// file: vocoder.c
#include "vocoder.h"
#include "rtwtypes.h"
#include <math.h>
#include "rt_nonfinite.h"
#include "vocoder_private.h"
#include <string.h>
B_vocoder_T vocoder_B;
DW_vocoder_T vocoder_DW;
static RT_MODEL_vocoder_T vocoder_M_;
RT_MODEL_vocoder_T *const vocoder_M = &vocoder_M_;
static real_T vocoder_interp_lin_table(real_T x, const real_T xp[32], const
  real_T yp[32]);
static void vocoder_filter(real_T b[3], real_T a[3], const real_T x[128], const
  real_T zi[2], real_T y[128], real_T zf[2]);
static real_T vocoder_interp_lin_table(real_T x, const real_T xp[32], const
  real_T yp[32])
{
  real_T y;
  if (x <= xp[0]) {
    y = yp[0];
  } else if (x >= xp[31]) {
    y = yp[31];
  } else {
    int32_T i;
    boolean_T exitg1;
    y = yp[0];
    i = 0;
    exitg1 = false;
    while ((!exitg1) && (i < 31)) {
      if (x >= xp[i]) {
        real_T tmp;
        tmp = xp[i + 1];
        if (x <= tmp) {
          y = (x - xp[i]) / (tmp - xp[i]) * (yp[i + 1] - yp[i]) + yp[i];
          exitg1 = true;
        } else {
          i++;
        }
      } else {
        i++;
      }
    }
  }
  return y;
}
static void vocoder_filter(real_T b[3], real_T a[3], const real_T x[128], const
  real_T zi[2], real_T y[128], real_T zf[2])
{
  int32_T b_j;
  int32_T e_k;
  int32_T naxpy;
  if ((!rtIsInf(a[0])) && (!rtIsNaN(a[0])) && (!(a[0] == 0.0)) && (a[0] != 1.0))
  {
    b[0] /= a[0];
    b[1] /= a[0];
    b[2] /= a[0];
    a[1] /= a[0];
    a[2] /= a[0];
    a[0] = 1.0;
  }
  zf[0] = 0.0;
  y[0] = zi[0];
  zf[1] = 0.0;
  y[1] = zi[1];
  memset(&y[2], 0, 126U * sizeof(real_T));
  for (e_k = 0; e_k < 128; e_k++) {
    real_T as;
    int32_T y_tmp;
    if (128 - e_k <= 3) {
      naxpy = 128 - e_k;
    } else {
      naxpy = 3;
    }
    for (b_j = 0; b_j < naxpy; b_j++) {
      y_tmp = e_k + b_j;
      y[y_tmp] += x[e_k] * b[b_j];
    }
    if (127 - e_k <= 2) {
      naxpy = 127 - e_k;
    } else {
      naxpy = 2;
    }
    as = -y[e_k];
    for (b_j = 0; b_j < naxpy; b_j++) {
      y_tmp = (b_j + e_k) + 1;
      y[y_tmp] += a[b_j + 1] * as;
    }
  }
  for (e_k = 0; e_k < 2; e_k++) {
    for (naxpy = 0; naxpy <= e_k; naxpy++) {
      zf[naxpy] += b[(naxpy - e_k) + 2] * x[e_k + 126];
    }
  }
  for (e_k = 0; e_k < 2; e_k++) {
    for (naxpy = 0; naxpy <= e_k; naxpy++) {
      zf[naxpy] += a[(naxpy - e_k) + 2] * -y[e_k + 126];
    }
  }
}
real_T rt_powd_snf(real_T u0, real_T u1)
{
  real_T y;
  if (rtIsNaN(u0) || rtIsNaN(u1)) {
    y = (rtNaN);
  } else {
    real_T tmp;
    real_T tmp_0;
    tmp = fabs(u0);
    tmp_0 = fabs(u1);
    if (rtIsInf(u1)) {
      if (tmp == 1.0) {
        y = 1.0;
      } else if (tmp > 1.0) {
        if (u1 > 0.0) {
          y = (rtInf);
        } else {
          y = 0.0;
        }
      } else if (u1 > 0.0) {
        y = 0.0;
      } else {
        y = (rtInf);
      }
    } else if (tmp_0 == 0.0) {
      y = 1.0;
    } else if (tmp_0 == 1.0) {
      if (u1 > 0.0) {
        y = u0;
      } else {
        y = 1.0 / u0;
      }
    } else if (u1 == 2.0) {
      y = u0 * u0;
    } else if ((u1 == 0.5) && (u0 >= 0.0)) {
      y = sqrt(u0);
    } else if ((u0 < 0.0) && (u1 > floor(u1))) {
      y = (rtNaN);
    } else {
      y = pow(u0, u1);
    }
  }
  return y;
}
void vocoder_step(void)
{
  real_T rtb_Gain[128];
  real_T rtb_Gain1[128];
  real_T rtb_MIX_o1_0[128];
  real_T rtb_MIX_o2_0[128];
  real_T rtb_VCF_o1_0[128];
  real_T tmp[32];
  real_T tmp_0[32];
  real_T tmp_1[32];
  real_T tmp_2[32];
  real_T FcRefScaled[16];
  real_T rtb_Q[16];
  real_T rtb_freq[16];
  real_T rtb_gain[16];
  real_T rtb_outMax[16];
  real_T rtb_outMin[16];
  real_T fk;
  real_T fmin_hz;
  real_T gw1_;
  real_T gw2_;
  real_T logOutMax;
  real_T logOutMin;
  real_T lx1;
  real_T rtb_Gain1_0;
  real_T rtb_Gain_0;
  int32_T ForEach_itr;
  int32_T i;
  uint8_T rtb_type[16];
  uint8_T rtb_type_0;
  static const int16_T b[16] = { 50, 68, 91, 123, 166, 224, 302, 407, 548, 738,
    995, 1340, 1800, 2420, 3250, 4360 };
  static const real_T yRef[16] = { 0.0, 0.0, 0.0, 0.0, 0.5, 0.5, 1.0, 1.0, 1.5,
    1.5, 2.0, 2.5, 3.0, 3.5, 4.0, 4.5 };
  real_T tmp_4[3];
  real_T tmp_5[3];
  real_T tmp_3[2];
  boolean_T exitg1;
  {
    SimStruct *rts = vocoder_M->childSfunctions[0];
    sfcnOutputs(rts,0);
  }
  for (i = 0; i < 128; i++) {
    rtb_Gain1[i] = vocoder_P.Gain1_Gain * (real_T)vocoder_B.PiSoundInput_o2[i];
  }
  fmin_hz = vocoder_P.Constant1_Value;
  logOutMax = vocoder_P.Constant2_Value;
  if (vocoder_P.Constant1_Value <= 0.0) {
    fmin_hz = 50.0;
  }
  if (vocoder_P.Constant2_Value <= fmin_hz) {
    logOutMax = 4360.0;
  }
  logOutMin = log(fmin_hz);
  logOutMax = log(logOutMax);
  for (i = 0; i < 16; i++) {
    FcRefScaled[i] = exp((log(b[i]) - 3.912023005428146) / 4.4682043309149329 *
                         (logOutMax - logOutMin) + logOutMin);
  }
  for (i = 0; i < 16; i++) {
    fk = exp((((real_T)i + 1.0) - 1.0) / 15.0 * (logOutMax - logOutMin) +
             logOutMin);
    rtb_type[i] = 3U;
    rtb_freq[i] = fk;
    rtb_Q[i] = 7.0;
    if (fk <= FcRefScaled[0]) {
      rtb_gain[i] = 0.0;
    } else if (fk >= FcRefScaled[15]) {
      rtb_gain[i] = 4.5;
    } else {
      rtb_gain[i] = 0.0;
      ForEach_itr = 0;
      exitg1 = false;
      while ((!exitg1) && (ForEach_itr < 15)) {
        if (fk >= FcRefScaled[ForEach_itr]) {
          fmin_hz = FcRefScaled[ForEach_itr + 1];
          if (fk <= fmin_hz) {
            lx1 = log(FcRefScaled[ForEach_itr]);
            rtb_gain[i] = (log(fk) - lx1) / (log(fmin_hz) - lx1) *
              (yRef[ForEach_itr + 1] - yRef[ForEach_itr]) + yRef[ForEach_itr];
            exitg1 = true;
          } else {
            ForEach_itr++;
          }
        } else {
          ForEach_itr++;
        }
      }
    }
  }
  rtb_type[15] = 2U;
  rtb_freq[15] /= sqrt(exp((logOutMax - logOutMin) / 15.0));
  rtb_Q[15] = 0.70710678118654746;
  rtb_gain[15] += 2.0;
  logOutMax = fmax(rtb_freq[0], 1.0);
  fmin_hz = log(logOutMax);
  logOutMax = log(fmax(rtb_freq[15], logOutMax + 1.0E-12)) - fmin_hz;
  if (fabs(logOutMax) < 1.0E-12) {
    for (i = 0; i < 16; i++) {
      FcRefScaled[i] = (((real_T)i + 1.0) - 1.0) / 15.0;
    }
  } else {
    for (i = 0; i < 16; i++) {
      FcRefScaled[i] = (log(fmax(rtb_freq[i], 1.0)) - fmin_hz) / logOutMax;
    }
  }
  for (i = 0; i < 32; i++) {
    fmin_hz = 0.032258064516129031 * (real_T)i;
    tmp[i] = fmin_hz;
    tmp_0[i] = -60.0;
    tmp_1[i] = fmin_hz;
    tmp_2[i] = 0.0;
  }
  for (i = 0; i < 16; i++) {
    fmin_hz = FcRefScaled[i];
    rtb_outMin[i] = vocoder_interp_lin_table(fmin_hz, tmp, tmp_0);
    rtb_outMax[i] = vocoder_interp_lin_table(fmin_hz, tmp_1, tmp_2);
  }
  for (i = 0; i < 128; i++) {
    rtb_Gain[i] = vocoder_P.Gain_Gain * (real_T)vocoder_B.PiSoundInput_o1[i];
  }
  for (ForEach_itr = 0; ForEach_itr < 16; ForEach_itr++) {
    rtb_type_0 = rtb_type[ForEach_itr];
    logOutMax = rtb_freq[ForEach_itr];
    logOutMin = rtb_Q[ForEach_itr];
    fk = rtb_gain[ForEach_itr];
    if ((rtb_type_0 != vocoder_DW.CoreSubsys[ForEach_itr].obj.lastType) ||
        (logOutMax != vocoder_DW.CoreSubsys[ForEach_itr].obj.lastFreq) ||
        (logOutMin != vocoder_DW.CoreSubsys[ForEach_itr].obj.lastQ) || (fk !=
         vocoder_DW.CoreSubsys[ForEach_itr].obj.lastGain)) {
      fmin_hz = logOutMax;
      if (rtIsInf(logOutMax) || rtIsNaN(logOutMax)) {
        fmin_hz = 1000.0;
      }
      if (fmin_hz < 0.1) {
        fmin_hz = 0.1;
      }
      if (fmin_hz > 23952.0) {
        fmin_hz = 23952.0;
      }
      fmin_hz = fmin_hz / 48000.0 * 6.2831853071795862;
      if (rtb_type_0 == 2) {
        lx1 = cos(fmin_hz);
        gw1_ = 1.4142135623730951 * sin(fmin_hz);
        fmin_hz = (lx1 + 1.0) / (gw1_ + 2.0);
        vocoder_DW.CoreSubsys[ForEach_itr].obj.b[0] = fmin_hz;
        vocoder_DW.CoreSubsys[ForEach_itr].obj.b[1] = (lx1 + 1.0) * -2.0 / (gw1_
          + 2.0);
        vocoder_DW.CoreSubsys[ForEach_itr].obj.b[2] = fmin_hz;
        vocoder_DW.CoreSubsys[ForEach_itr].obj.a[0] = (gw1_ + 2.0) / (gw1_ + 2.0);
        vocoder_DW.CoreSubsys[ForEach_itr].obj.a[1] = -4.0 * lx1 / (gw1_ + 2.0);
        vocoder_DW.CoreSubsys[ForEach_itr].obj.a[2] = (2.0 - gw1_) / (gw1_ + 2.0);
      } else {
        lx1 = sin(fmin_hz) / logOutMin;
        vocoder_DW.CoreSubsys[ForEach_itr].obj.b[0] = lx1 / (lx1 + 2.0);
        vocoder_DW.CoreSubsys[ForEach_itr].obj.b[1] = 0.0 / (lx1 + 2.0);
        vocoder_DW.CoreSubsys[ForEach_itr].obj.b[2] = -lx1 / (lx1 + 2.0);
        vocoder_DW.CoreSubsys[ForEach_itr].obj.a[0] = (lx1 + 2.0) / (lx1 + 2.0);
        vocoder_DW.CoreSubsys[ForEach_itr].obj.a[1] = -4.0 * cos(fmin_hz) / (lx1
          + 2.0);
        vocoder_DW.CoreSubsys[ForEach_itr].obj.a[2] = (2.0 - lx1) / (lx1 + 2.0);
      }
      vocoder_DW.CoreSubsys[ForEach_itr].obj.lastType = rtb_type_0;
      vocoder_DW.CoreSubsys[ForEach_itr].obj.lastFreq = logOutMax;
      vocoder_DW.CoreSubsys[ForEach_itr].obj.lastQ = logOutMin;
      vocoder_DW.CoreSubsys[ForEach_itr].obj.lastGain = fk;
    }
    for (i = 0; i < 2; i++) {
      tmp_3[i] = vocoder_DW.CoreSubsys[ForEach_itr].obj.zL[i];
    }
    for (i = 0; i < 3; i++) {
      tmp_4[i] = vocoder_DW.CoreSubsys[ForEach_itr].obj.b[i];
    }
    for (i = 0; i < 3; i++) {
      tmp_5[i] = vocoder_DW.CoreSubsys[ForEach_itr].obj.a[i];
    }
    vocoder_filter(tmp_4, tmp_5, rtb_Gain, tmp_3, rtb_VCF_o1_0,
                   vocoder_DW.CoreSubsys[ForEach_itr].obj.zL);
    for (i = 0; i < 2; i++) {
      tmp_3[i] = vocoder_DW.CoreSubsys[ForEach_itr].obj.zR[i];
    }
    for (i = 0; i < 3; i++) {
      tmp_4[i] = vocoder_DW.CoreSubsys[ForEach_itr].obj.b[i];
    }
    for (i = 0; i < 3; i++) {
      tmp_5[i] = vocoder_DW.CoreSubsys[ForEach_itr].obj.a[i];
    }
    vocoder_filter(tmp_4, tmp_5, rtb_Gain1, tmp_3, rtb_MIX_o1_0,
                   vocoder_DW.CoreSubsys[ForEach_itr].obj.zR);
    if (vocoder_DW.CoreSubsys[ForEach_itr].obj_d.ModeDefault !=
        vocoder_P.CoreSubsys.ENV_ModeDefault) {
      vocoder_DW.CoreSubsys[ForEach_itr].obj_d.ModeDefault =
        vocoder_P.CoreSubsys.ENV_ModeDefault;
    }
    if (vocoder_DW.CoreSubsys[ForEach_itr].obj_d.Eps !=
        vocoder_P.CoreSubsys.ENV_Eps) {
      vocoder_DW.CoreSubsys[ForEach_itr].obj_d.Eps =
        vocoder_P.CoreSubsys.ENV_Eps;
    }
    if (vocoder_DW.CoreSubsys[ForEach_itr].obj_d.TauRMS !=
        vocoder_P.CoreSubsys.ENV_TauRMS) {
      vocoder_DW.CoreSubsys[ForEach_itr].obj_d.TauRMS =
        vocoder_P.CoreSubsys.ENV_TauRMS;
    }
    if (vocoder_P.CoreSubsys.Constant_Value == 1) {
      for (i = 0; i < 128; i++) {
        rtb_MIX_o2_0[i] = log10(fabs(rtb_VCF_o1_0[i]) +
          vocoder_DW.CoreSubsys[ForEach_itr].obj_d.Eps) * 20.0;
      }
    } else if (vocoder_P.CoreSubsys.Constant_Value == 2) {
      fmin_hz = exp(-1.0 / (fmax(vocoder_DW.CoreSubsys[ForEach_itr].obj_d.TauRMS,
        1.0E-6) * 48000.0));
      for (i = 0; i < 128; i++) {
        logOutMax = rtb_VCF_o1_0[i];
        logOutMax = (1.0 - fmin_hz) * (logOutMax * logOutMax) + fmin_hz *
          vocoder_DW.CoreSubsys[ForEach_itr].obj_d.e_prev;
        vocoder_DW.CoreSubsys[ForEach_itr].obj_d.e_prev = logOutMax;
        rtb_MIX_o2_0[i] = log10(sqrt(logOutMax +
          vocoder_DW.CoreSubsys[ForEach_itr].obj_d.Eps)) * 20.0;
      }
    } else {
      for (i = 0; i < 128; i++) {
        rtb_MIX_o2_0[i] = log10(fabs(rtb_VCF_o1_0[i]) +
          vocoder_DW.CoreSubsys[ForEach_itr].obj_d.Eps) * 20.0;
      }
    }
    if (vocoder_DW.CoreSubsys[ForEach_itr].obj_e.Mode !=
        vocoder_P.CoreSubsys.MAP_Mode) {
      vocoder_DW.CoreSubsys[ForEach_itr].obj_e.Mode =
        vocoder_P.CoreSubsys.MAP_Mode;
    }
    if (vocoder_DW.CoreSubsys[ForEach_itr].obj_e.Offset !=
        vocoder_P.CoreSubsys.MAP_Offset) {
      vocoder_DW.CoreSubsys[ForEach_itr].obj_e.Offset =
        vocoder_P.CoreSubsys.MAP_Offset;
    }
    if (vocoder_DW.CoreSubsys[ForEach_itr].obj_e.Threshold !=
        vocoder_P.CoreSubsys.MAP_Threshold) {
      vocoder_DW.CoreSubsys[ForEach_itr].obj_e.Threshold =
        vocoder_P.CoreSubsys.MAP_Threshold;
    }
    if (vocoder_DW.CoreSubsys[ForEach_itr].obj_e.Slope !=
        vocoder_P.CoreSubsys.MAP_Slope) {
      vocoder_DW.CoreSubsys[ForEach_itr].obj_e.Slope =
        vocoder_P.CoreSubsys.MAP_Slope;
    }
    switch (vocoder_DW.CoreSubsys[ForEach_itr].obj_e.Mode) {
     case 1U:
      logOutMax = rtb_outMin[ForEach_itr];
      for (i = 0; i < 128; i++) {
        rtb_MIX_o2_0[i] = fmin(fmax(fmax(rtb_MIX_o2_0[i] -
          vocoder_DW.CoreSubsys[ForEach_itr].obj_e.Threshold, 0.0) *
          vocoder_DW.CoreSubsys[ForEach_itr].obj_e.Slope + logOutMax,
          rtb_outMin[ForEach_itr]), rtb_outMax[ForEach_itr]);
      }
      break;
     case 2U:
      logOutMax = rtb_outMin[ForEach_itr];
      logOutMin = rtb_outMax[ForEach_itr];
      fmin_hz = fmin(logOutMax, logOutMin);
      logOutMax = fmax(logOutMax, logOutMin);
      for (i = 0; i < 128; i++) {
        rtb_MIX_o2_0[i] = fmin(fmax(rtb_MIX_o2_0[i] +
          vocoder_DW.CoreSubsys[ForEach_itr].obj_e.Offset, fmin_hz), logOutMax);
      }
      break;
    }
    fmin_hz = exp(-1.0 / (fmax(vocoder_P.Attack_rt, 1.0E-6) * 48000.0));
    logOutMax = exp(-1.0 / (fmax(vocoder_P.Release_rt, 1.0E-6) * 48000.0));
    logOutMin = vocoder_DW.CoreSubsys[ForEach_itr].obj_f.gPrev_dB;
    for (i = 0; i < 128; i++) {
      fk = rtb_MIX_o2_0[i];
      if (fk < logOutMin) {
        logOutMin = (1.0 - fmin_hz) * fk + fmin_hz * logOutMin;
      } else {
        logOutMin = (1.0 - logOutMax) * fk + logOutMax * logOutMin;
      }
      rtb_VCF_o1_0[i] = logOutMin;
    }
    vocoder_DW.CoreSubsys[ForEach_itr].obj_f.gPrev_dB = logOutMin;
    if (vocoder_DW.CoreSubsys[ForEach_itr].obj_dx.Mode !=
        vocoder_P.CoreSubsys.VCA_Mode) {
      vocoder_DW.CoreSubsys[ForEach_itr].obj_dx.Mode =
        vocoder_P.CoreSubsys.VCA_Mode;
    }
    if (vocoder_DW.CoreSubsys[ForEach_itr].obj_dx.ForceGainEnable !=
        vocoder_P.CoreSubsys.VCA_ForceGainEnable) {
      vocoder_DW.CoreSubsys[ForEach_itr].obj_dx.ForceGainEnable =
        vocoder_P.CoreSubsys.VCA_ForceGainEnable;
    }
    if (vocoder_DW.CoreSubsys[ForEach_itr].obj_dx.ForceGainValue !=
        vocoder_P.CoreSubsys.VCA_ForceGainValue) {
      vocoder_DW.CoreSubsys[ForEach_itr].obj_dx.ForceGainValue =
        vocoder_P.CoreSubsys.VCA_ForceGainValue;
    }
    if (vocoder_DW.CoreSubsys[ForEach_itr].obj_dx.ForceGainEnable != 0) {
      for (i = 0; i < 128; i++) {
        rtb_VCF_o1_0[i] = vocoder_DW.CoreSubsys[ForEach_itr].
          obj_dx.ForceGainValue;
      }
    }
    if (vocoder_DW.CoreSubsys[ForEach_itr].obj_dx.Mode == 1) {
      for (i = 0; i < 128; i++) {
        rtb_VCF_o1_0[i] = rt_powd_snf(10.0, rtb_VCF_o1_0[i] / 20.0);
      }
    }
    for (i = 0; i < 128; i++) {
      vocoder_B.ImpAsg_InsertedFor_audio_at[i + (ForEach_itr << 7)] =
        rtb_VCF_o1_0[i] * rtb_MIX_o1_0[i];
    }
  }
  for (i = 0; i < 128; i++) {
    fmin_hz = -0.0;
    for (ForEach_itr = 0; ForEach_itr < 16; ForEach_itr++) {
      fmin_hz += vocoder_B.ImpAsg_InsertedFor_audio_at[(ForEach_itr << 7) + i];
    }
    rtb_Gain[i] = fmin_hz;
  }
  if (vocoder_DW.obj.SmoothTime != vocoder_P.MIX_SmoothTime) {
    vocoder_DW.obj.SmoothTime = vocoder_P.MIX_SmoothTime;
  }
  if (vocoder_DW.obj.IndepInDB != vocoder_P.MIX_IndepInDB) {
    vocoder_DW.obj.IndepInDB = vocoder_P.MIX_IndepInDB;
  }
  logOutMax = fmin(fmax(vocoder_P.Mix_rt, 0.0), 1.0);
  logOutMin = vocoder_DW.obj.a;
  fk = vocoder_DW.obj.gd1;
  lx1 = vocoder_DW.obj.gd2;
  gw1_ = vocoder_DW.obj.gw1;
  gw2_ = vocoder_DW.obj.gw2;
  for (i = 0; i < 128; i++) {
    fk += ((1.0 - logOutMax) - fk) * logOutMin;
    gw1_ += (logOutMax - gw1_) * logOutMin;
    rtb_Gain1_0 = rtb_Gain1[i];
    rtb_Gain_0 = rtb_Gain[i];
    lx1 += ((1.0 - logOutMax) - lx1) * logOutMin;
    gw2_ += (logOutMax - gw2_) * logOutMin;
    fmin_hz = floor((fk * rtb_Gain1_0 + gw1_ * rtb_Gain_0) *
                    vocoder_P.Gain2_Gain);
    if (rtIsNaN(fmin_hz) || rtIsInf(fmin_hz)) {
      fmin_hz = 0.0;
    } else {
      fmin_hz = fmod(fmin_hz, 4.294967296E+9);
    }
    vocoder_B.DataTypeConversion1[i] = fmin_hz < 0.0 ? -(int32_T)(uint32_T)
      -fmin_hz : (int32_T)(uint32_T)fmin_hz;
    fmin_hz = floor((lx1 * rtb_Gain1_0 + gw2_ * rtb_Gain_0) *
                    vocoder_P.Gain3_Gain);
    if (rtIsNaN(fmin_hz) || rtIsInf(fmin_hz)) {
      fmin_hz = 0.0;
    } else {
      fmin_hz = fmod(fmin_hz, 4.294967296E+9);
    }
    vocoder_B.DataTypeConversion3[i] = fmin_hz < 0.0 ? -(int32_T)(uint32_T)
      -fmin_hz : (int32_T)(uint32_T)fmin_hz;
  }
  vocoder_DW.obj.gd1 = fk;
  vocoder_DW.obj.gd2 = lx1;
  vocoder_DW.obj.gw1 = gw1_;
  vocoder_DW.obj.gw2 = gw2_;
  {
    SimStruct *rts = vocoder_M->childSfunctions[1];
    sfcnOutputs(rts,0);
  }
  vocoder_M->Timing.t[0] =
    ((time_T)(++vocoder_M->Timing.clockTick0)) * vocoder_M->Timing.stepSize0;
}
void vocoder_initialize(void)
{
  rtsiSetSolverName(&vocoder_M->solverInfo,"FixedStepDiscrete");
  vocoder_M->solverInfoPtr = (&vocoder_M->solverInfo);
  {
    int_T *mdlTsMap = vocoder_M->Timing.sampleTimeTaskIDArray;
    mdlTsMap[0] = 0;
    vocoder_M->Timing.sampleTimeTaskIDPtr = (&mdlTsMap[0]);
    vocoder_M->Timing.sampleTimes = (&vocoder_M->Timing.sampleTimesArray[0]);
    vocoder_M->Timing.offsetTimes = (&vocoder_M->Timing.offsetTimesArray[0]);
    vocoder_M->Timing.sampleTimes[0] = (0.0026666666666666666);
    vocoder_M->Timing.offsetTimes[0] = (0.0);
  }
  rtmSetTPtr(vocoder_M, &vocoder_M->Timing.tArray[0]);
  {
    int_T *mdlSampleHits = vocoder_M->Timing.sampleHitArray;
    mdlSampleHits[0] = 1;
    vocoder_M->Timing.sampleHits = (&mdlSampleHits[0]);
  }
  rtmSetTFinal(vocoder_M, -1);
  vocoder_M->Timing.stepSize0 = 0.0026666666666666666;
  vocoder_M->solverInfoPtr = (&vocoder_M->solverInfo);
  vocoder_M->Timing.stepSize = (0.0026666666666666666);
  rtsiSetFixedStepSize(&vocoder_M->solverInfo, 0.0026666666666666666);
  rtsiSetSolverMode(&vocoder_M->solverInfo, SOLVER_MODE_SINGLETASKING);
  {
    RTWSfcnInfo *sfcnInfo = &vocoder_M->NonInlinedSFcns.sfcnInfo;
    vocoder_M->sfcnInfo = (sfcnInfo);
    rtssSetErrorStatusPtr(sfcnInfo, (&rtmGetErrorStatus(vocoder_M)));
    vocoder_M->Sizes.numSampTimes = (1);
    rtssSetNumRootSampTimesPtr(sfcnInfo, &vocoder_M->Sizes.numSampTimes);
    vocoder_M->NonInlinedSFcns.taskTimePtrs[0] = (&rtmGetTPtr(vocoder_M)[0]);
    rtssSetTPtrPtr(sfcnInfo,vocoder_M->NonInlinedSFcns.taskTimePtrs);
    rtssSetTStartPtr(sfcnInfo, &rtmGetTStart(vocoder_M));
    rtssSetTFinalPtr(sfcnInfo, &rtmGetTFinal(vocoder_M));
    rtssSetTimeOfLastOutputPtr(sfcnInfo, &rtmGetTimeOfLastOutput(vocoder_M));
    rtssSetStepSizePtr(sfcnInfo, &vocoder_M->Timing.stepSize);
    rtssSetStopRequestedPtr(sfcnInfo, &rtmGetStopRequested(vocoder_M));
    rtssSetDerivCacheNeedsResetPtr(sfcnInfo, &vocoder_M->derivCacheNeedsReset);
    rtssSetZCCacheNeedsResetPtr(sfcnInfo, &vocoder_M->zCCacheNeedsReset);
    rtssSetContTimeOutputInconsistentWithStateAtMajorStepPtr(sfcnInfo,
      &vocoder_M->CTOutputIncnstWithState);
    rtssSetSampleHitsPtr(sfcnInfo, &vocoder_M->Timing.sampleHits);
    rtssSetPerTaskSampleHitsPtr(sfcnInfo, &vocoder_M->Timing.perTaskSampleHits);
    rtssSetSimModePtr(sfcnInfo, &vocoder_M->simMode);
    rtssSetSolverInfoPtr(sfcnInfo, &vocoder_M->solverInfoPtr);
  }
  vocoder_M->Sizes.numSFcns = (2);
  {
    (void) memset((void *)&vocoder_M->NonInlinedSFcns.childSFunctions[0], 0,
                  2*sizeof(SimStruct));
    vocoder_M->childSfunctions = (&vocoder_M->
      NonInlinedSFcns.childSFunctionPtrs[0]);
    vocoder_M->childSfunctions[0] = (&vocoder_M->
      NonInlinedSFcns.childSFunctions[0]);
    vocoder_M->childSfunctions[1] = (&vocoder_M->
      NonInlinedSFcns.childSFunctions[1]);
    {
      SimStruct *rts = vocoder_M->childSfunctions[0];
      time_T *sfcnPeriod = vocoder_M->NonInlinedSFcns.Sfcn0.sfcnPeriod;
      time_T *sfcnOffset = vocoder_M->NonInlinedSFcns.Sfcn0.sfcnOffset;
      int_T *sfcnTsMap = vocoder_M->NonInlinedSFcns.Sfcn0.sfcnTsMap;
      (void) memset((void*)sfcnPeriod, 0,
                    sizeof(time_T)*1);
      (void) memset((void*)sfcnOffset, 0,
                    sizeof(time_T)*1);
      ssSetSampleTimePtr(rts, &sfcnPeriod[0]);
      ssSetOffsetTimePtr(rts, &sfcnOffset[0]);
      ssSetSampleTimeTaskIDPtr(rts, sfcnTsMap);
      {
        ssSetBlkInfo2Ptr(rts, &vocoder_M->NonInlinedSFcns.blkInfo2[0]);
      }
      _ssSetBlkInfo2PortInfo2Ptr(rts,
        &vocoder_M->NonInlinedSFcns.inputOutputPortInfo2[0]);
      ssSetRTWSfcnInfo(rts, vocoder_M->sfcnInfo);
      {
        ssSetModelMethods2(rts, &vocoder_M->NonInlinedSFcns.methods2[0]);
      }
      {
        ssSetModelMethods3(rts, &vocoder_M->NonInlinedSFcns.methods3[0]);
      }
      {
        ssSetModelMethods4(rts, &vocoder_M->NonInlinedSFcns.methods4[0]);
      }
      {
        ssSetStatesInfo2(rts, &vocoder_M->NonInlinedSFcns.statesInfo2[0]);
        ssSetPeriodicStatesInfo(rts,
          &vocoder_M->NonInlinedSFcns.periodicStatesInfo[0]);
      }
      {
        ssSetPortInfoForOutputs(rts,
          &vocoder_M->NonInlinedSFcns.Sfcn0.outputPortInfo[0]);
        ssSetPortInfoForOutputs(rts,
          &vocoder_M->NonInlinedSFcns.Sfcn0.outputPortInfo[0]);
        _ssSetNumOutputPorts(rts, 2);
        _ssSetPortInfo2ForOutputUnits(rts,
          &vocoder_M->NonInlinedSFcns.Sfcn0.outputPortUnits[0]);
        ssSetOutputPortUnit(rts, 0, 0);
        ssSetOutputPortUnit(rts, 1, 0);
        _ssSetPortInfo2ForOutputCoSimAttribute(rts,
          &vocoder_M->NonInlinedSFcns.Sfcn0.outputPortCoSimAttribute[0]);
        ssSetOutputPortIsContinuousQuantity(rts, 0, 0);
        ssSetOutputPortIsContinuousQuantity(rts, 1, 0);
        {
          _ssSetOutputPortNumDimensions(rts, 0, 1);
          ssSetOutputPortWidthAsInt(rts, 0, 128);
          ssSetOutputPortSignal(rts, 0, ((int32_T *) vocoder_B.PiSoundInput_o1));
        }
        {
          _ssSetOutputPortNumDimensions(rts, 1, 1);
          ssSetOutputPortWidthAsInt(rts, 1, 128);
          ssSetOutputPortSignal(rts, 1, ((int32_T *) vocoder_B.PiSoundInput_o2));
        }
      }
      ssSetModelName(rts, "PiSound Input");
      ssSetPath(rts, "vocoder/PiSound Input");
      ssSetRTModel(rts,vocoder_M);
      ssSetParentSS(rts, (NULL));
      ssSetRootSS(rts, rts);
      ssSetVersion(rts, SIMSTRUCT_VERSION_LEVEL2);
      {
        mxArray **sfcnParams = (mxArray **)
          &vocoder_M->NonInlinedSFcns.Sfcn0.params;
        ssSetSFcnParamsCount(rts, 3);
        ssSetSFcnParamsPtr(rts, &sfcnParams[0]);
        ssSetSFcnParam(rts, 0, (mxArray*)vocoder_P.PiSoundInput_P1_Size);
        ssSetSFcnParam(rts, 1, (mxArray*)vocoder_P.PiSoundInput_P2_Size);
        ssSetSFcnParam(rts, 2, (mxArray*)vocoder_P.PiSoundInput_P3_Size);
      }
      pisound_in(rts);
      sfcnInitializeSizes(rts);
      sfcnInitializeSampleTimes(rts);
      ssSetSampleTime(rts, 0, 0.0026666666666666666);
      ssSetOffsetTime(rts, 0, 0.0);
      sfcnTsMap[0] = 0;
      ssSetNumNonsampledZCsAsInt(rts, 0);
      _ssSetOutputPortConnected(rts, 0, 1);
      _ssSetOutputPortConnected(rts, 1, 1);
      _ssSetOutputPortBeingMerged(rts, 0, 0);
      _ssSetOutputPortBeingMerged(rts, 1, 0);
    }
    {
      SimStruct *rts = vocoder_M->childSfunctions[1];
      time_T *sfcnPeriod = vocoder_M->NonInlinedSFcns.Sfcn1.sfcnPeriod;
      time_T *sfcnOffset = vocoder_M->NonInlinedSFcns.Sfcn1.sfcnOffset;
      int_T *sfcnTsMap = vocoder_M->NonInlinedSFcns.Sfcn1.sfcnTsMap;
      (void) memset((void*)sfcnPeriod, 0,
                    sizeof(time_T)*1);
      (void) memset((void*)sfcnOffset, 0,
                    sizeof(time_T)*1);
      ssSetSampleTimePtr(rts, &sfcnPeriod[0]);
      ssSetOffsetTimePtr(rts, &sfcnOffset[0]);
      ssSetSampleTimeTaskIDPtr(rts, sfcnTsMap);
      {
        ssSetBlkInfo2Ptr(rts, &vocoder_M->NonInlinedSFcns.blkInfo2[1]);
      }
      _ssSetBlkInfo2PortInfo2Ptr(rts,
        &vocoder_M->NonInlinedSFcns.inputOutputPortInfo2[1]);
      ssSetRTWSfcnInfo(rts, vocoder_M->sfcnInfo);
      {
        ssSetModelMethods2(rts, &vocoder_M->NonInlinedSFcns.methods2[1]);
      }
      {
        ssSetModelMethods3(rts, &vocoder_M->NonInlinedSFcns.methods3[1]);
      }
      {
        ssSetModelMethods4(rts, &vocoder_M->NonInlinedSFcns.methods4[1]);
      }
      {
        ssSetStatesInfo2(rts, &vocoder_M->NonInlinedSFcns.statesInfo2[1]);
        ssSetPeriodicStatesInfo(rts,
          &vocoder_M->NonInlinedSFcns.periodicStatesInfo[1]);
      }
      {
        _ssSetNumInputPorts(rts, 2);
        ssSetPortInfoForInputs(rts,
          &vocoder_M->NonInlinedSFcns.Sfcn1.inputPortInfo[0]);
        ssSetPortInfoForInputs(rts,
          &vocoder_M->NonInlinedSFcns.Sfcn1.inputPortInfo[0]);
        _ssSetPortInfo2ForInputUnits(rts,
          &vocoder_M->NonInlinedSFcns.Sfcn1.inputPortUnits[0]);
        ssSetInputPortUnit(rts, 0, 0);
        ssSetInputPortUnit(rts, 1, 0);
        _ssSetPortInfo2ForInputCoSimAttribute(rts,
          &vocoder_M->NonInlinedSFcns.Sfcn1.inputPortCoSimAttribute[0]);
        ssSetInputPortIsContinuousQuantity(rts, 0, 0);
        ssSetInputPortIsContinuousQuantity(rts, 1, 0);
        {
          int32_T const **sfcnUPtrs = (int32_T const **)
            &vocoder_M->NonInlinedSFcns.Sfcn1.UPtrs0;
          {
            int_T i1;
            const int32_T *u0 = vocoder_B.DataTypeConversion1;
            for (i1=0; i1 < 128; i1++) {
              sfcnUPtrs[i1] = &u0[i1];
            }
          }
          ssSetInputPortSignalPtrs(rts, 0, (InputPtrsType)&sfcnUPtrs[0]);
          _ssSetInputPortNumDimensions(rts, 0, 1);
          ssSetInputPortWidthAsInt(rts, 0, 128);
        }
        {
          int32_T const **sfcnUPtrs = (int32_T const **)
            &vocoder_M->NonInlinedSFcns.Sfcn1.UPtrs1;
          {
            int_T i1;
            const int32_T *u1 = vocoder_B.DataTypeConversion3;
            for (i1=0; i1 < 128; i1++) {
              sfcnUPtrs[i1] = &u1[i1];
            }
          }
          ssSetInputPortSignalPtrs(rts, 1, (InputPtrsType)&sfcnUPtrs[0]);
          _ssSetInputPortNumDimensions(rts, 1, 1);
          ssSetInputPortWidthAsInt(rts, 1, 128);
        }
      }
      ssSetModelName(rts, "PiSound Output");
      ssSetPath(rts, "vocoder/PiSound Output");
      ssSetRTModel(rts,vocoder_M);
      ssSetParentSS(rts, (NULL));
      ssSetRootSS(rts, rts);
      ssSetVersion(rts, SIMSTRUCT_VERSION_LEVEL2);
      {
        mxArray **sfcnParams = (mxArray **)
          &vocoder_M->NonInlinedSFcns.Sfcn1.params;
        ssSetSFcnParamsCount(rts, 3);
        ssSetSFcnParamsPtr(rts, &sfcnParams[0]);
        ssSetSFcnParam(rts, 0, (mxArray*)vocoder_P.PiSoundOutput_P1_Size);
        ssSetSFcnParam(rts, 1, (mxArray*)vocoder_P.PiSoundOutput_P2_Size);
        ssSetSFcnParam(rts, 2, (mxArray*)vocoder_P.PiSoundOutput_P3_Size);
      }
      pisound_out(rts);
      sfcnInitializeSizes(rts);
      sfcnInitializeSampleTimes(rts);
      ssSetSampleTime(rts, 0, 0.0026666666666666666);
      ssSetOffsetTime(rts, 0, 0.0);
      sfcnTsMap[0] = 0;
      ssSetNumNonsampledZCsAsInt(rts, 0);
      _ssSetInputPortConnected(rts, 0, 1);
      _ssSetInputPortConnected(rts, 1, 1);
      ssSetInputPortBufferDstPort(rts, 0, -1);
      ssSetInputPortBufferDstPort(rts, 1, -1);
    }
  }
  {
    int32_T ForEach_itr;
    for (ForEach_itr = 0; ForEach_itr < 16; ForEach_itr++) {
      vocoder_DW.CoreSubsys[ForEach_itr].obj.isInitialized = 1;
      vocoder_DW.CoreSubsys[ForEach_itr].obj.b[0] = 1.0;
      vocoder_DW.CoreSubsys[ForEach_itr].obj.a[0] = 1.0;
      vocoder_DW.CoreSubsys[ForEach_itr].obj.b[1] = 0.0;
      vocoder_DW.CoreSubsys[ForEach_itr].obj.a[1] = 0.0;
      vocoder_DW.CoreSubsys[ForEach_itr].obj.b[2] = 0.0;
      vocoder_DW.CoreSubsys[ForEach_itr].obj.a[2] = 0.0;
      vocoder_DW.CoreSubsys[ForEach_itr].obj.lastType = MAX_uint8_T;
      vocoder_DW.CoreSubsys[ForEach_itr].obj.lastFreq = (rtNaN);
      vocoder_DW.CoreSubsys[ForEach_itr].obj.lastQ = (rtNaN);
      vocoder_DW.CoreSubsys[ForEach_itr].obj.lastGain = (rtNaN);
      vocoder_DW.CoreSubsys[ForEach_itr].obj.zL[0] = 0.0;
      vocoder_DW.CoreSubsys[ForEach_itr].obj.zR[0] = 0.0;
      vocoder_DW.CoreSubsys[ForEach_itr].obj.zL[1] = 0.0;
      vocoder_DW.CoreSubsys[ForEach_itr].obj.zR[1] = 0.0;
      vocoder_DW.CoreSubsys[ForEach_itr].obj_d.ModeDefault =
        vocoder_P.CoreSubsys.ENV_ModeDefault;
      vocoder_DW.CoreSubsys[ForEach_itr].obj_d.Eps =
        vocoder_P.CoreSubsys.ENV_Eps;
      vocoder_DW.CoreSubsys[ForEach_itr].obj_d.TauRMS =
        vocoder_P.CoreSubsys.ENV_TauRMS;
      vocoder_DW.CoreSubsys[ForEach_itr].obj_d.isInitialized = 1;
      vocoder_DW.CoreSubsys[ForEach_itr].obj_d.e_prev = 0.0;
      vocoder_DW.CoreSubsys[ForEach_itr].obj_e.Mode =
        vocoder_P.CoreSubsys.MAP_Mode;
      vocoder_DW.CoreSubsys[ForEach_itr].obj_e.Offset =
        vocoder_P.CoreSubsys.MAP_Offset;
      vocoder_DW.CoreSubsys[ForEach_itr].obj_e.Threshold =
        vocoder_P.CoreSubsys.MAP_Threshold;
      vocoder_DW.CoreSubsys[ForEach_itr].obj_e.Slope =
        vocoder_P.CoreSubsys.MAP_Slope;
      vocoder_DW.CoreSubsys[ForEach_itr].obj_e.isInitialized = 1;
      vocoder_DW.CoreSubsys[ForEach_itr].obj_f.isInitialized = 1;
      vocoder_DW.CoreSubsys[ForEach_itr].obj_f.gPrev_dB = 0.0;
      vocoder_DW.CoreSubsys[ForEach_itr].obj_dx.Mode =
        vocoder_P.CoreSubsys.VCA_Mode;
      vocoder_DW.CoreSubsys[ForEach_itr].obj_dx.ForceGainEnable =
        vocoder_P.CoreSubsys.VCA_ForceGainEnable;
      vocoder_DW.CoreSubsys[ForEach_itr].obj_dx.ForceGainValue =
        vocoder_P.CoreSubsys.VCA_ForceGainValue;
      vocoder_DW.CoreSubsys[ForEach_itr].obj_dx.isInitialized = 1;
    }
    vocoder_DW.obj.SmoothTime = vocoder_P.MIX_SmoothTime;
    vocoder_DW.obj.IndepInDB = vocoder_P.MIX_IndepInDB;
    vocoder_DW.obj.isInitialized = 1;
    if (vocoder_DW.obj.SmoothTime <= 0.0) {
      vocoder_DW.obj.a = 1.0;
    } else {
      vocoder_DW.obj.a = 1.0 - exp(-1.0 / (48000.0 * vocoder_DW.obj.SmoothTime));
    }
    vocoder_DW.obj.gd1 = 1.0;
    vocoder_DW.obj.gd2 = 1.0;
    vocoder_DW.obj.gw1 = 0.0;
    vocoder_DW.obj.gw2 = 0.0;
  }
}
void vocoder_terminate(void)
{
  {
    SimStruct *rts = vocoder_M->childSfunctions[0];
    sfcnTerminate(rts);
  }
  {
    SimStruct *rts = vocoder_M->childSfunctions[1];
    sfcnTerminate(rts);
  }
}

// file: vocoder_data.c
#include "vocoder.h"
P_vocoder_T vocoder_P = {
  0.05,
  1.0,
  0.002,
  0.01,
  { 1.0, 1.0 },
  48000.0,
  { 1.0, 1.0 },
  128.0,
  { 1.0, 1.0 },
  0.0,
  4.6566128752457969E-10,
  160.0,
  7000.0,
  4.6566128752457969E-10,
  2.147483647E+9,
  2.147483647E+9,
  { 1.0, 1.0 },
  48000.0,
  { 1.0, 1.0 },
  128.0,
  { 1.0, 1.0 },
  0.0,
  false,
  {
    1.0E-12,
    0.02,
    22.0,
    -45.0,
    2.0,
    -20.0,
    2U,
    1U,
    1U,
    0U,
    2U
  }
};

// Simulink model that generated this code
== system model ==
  PiSoundOutput : S-Function  FunctionName=pisound_out  <- 1: DataTypeConversion1, 2: DataTypeConversion3
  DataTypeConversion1 : DataTypeConversion  <- 1: Gain2
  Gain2 : Gain  Gain=2^31-1  <- 1: MIX
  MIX : MATLABSystem  N=128  <- 1: Gain1, 2: Gain1, 3: Sum#1, 4: Sum#1, 5: Constant#1
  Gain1 : Gain  Gain=1/(2^31-1)  <- 1: DataTypeConversion#1
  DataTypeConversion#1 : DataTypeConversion  <- 1: PiSoundInput/2
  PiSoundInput : S-Function  FunctionName=pisound_in
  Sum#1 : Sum  Inputs=+  <- 1: Subsystem#1
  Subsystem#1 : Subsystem  <- 1: MATLABFunction#1, 2: MATLABFunction#1/2, 3: MATLABFunction#1/3, 4: MATLABFunction#1/4, 5: Gain, 6: Gain1, 7: MATLABFunction#1/5, 8: MATLABFunction#1/6
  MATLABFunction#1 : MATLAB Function  <- 1: Constant1, 2: Constant2
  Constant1 : Constant  Value=160
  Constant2 : Constant  Value=7000
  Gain : Gain  Gain=1/(2^31-1)  <- 1: DataTypeConversion#2
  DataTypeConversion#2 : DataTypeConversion  <- 1: PiSoundInput
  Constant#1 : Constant  Value=Mix_rt
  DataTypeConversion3 : DataTypeConversion  <- 1: Gain3
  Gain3 : Gain  Gain=2^31-1  <- 1: MIX/2
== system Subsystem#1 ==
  type : Inport
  freq : Inport
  Inport#1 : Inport
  gain : Inport
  Inport#2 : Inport
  Inport#3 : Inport
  outMin : Inport
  outMax : Inport
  ForEach : ForEach
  audio : Outport  <- 1: VCA
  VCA : MATLABSystem  N=128  <- 1: VCF/2, 2: MATLABSystem#1
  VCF : MATLABSystem  N=128  <- 1: Inport#2, 2: Inport#3, 3: type, 4: freq, 5: Inport#1, 6: gain
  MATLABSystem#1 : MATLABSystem  N=128  <- 1: MAP, 2: Constant#2, 3: Constant#3
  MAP : MATLABSystem  Threshold=-45  <- 1: ENV, 2: outMin, 3: outMax
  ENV : MATLABSystem  N=128  <- 1: VCF, 2: Constant
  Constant : Constant  Value=2
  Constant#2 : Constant  Value=Attack_rt
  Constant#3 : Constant  Value=Release_rt
== matlab function MATLABFunction#1 ==
function [type,freq,Q,gain,outMin,outMax] = vocoder_params(fmin,fmax)
%#codegen
  K = int32(16);
  [type,freq,Q,gain] = fb_params(fmin,fmax,K);
  [outMin,outMax] = ctrl_params_from_freq(freq,K);
  type = type(1:K);
  freq = freq(1:K);
  Q    = Q(1:K);
  gain = gain(1:K);
end
